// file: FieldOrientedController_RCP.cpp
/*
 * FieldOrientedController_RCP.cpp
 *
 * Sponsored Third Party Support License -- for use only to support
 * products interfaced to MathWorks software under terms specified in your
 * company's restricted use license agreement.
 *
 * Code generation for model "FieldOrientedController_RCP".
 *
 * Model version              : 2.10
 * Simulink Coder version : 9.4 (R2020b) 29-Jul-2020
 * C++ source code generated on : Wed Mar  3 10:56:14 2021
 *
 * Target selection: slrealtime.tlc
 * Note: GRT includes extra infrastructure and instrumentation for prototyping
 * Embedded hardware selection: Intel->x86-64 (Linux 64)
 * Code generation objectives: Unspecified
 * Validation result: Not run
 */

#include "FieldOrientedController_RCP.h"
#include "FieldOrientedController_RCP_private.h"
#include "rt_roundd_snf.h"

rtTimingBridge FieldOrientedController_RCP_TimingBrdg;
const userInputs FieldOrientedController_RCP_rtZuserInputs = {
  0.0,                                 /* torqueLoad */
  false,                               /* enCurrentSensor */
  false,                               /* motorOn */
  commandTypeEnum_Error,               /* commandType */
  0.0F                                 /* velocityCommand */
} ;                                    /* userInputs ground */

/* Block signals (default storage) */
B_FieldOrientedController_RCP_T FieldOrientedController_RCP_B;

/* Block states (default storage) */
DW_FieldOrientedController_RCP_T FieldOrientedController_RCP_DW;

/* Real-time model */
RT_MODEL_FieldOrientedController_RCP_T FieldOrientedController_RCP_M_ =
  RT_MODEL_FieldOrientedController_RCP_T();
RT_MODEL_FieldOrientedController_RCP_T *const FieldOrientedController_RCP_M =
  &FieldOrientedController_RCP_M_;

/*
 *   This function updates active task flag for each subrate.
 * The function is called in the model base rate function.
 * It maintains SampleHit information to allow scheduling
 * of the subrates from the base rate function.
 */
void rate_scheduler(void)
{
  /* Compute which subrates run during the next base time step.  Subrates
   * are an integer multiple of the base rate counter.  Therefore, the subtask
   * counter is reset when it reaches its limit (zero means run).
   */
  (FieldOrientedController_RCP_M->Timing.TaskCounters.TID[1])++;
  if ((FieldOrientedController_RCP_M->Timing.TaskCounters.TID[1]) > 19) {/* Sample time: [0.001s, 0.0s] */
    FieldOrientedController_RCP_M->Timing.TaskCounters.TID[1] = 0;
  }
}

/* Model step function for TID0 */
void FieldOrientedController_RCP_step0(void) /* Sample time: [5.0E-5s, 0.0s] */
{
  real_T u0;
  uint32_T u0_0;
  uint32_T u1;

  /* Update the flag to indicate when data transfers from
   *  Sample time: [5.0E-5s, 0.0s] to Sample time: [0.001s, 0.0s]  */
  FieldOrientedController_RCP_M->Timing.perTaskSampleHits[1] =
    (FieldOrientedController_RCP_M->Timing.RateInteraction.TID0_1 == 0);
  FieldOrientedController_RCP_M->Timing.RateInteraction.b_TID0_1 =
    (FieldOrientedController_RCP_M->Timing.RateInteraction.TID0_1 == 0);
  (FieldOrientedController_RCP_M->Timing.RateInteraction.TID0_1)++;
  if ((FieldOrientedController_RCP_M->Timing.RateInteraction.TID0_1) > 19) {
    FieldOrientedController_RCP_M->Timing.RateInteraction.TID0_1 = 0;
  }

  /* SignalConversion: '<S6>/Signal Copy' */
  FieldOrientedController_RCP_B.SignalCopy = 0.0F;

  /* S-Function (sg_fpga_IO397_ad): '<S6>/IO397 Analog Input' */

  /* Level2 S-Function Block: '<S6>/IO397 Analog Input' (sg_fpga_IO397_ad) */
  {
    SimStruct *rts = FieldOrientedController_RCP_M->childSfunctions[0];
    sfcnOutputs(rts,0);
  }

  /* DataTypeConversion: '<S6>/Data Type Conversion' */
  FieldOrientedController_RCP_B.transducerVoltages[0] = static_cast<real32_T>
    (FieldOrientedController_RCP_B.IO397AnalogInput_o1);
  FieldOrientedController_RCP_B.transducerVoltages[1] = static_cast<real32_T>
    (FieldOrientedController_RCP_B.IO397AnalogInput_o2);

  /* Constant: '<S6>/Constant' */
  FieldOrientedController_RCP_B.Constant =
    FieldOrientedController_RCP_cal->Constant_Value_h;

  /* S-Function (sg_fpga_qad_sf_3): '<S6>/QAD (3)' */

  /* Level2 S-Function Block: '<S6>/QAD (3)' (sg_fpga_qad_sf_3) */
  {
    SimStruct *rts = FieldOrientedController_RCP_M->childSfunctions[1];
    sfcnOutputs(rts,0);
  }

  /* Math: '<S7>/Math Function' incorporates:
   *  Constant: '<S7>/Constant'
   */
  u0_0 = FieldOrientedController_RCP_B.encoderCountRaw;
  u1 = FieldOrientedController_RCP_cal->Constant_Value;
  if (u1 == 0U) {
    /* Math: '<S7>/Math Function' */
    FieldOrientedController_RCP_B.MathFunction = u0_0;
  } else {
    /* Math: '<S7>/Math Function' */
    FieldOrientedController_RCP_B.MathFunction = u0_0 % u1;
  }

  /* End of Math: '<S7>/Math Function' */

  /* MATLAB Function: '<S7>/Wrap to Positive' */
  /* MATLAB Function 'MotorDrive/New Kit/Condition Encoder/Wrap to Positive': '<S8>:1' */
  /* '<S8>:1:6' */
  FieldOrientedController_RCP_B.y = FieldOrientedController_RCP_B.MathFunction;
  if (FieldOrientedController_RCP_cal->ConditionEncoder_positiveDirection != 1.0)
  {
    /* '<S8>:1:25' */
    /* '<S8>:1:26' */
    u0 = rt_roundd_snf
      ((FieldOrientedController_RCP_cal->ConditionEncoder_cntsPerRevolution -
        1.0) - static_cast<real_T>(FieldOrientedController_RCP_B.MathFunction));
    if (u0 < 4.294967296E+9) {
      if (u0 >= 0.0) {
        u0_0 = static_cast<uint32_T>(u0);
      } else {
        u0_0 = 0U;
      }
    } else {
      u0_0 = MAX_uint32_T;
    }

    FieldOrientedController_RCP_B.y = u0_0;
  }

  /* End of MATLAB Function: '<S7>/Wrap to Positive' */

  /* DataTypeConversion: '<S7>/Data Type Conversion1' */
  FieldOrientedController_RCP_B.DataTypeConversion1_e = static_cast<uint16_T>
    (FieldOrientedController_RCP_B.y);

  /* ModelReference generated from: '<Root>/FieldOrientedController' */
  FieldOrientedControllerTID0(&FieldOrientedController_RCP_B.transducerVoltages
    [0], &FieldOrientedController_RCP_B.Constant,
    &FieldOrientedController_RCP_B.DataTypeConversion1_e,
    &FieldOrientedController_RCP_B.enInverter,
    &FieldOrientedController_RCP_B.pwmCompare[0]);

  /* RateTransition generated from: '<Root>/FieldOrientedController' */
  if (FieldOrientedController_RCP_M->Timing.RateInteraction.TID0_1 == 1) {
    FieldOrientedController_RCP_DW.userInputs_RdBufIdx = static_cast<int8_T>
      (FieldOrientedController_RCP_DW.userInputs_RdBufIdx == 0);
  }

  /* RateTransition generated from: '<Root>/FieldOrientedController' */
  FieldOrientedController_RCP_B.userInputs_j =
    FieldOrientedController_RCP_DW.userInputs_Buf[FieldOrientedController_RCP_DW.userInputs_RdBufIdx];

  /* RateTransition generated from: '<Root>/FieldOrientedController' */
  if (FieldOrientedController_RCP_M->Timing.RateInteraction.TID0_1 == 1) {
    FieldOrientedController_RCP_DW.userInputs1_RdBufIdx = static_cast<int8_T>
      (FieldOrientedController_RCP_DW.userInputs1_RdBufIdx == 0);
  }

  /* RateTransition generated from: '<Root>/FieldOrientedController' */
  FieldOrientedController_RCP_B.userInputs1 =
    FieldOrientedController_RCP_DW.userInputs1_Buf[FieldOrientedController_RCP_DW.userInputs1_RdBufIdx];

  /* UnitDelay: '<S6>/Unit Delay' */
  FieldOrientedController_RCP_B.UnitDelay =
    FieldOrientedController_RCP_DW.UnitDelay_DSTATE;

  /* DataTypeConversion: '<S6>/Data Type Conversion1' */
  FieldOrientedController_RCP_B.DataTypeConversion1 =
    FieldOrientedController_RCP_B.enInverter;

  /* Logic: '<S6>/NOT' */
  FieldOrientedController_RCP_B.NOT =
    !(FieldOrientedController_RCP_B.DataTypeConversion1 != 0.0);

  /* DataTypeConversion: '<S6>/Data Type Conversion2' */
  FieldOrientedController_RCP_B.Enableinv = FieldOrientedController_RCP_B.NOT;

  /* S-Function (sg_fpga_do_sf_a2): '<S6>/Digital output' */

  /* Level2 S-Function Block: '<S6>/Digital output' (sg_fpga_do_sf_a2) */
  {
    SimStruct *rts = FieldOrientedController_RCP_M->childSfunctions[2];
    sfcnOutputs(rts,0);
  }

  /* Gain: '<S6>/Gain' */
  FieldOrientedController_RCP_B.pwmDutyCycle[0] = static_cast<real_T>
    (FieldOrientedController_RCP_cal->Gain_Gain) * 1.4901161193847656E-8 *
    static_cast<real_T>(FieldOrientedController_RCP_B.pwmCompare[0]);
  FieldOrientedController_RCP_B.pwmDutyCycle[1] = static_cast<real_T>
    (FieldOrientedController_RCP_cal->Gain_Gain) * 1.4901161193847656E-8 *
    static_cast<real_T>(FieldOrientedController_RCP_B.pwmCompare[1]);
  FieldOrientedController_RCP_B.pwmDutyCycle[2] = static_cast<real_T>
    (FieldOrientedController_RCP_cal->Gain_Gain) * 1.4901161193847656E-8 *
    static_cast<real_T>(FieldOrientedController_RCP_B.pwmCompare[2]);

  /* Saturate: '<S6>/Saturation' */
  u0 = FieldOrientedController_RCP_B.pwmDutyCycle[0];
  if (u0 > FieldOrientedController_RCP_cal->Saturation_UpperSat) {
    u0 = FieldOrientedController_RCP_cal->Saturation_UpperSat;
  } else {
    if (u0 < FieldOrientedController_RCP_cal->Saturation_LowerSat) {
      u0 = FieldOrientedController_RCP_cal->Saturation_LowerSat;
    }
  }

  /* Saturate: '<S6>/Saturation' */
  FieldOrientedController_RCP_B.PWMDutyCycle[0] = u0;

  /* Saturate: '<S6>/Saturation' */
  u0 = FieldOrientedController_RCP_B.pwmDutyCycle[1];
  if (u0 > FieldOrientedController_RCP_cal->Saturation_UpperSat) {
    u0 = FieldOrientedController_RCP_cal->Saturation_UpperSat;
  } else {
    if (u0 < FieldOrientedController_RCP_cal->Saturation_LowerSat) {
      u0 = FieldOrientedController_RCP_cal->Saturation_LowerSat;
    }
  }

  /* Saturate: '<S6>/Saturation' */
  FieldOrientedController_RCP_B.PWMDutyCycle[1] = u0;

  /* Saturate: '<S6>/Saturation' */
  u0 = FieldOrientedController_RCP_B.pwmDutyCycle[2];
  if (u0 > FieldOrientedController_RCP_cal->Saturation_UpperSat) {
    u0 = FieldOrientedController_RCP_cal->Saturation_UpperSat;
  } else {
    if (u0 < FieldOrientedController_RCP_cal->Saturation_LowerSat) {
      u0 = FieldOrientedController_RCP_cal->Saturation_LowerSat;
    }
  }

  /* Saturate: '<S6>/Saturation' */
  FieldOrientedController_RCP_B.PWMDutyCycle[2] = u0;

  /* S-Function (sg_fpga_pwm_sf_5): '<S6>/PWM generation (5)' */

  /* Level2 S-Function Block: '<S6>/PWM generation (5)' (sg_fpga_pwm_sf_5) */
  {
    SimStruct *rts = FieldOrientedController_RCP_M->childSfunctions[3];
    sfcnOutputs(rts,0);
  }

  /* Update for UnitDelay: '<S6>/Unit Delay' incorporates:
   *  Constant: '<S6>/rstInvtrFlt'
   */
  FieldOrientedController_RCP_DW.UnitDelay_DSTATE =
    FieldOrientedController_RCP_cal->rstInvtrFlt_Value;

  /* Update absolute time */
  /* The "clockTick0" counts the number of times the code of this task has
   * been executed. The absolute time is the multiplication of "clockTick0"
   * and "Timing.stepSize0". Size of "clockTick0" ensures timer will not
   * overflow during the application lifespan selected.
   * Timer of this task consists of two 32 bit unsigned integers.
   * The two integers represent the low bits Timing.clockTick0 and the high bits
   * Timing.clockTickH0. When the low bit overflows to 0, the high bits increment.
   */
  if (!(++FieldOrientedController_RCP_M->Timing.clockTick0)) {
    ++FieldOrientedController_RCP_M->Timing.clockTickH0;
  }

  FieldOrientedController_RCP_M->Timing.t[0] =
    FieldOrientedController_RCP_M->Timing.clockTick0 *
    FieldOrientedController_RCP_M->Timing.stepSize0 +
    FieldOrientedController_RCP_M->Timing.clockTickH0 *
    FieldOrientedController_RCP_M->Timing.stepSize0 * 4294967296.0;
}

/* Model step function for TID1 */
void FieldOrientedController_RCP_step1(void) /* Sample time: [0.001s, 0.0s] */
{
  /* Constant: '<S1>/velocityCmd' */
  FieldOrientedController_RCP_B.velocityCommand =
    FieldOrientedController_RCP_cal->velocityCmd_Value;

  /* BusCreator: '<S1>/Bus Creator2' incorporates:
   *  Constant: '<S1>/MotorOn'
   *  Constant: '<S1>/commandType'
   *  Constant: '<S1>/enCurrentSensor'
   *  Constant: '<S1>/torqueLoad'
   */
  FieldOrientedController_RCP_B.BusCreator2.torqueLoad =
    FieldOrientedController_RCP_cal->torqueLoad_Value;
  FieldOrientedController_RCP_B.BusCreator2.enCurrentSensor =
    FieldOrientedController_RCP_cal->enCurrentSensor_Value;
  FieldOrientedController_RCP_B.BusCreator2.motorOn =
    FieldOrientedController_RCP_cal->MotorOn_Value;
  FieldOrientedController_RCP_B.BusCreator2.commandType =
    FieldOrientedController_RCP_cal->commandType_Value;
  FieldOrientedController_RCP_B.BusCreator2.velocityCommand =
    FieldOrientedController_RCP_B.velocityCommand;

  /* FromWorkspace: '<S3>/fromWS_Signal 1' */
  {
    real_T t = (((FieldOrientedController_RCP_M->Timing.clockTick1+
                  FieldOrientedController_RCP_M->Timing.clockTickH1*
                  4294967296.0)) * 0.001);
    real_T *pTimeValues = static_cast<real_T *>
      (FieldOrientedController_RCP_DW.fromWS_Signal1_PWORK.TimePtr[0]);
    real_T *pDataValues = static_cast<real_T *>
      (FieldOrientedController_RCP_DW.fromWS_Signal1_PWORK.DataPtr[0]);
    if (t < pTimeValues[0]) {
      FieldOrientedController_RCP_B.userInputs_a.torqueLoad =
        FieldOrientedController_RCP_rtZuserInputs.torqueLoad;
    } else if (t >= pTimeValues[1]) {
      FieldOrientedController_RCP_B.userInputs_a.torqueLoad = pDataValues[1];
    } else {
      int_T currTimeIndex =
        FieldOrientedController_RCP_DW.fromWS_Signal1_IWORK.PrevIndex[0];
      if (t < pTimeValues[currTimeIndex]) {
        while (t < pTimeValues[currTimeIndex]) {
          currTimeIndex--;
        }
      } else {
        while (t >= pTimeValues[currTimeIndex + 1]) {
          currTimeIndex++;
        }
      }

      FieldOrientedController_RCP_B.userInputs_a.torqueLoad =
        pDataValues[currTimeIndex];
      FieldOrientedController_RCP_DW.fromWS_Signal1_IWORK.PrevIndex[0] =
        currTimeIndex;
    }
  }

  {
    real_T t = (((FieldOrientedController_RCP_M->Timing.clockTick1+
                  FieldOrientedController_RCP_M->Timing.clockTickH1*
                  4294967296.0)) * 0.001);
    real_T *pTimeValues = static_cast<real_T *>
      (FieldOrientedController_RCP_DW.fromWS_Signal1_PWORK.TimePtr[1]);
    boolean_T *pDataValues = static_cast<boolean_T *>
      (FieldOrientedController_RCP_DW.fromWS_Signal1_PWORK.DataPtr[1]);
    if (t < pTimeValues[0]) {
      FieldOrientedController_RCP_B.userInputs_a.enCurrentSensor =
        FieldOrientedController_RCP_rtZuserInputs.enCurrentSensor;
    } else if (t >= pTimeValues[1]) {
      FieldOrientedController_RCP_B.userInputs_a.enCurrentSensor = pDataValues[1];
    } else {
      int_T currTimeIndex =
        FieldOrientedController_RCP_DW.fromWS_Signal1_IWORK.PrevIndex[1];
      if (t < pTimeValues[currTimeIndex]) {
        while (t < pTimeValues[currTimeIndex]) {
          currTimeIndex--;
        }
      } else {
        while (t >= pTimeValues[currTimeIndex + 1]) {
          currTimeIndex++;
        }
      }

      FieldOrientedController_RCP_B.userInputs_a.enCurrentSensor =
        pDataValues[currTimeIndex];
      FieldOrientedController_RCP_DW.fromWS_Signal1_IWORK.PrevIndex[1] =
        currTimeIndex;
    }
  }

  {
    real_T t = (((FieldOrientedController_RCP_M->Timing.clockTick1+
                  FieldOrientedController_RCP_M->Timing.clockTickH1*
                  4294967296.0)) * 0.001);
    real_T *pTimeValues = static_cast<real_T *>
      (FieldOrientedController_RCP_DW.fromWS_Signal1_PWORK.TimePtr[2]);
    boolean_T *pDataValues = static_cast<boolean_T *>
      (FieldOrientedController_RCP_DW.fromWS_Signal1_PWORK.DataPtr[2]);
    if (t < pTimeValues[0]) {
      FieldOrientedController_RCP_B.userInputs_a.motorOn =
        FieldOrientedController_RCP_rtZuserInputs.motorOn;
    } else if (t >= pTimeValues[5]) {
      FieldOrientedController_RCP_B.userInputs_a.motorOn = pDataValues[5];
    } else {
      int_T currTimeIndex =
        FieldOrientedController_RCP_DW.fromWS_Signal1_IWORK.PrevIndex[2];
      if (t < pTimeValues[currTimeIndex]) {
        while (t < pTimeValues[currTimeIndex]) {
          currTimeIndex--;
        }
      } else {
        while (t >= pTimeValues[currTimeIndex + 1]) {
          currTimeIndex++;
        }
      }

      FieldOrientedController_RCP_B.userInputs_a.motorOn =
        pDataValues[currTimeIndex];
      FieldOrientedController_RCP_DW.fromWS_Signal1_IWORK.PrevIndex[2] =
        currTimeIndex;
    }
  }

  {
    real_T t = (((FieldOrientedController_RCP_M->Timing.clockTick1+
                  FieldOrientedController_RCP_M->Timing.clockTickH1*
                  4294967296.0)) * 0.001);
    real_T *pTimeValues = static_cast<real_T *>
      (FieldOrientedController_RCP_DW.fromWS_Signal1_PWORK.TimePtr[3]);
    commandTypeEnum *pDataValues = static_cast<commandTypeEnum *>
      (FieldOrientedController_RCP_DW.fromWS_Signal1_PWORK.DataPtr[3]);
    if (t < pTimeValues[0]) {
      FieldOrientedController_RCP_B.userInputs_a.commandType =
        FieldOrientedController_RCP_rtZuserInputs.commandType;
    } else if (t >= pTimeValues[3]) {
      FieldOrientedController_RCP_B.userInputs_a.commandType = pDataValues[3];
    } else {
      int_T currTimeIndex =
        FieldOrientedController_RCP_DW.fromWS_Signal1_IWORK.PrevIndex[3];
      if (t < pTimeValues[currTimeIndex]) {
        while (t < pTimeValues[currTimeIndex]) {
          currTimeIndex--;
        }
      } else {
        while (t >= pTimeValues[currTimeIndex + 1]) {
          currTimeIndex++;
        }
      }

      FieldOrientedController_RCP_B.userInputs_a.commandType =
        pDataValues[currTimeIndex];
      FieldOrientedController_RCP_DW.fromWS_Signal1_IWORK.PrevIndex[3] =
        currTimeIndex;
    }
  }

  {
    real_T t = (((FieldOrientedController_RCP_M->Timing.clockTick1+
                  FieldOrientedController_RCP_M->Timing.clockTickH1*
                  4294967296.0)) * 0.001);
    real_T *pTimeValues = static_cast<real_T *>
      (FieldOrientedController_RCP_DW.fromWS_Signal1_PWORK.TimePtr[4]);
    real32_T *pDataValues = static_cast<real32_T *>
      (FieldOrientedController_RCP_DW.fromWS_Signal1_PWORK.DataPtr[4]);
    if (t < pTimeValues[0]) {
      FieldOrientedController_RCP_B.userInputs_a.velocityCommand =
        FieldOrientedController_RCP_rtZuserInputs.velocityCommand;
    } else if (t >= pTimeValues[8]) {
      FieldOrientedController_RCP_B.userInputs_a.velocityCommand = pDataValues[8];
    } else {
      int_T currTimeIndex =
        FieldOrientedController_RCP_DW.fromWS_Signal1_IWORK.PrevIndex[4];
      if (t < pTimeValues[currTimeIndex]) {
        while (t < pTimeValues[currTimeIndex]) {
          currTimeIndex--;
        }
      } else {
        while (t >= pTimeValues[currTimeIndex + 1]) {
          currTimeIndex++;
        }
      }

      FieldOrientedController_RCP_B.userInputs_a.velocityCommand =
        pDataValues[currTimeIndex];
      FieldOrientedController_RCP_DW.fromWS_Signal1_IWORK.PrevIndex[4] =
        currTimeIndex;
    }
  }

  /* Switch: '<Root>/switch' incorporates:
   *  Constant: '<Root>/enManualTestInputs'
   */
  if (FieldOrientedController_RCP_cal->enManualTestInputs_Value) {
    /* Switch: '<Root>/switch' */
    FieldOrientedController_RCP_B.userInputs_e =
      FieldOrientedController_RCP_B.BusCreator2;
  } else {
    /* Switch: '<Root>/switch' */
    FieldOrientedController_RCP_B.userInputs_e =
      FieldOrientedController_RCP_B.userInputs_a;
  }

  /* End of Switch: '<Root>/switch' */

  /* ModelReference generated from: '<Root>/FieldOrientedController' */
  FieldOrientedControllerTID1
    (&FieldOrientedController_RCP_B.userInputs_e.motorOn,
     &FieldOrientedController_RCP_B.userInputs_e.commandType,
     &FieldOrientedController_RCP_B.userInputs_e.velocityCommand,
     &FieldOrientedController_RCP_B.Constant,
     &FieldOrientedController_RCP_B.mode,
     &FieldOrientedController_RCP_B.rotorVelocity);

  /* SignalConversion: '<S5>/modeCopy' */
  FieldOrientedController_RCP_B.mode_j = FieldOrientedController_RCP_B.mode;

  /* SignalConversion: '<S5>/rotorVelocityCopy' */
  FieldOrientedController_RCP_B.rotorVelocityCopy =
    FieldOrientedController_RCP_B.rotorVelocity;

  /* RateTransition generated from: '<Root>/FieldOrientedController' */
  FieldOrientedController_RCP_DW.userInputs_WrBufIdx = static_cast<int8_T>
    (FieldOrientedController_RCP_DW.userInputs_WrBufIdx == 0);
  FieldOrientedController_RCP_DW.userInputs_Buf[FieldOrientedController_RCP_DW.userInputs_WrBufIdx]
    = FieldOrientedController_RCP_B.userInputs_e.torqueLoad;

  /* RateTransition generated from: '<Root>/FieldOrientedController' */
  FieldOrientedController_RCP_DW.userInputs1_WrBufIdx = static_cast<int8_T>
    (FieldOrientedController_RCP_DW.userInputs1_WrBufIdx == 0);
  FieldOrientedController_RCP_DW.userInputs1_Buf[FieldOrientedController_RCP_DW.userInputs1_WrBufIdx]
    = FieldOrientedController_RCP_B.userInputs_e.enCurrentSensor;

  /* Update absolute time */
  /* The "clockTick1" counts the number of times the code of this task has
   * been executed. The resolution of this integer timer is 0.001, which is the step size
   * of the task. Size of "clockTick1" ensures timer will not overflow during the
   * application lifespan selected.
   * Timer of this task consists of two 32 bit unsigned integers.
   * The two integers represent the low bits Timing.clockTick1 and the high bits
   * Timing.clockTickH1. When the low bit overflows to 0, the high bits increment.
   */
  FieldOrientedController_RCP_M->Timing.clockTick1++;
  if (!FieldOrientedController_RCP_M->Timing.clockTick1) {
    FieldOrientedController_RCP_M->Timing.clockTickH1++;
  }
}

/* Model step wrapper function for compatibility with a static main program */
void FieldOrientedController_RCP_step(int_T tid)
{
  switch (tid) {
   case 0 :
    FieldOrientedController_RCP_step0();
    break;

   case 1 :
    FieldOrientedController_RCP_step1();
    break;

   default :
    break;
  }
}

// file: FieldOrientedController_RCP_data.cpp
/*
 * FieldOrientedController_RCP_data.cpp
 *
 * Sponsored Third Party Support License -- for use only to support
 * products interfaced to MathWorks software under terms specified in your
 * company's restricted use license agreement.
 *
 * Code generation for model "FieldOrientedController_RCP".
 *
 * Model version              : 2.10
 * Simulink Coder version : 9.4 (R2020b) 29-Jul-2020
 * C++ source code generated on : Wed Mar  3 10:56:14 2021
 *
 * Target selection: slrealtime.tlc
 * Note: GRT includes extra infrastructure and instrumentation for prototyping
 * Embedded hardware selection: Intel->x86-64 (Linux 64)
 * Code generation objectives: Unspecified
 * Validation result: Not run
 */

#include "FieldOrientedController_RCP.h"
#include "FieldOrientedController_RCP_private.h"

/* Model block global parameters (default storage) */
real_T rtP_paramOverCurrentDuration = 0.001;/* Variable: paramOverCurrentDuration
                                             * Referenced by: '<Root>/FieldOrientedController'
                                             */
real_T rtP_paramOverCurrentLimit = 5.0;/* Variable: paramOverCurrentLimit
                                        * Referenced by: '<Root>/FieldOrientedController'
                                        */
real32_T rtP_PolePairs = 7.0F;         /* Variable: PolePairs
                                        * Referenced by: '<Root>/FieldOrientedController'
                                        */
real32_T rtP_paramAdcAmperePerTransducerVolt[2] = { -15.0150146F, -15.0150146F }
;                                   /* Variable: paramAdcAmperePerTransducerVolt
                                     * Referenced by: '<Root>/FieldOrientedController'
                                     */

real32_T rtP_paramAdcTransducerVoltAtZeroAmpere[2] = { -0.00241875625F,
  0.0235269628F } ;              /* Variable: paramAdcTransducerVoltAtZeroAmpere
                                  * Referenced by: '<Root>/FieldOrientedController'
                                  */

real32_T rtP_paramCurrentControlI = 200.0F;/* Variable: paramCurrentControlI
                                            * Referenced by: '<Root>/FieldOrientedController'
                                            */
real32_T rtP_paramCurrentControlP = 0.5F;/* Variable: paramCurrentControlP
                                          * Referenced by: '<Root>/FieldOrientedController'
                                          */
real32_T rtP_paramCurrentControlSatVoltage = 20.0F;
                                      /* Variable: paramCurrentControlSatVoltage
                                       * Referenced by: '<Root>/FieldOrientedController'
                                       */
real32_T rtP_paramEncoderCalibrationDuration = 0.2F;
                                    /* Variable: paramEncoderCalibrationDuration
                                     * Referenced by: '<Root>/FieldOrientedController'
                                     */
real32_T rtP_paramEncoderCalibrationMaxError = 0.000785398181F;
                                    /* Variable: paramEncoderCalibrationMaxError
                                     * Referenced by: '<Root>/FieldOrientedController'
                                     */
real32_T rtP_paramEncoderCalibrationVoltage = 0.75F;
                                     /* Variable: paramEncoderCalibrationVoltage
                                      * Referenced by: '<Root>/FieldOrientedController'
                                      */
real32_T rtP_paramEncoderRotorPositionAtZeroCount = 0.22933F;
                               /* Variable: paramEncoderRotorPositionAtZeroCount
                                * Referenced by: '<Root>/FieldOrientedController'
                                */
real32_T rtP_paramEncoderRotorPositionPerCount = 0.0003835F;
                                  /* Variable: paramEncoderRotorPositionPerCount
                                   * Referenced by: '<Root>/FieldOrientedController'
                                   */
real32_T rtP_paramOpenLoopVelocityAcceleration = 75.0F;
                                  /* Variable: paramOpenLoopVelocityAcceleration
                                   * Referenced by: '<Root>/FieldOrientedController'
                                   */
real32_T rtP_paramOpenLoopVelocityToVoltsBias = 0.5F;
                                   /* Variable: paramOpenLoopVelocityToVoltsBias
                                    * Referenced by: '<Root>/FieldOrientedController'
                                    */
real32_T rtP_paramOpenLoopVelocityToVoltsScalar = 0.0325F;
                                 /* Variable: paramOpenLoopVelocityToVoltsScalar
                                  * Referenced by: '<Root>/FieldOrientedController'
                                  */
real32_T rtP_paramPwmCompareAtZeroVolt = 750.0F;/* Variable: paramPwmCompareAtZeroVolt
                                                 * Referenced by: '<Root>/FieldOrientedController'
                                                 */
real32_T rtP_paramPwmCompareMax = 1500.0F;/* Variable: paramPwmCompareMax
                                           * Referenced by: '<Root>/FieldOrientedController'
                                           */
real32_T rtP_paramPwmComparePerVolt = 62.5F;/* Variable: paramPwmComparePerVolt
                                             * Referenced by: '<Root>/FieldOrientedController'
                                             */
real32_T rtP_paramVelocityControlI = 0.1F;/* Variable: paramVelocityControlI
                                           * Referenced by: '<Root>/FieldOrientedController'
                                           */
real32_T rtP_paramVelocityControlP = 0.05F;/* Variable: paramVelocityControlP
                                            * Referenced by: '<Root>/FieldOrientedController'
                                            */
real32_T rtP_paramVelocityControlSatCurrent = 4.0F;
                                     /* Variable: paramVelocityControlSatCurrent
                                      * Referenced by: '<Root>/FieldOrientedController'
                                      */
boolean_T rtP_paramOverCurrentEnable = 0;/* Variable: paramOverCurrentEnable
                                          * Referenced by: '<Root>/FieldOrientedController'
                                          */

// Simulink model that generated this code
simulink model "FieldOrientedController_RCP"  (R2020b)
settings: configuration reference "SLRT" (kept outside this file)
undefined symbols (not defined in the file): commandTypeEnum, encoder, IO397, pwm, sampleTime
libraries: speedgoatlib_fpga_dio x2, speedgoatlib_fpga_analog_io x2, speedgoatlib_fpga_pwm x2, speedgoatlib_fpga_quadrature x2, speedgoatlib_fpga x2, SignalEditorBlockLib x1

== system FieldOrientedController_RCP ==
  Callback Button : CallbackButton  ButtonText=Switch Electric Motor Control Kit
  FieldOrientedController : ModelReference  ModelNameDialog=FieldOrientedController  SimulationMode=Normal  ModelReferenceVersion=1.564
  ManualTestInputs : Subsystem  Description=""  VariantControl=TestInputChoice == 2
  MotorDrive : Subsystem  Variant=on  VariantControl=demoMode == 2
  SignalEditor_Experiments : SignalEditorBlockLib/Signal Editor  FileName=PMSM_Experiments.mat  ActiveScenario=ClosedLoop_CoastdownTest  ActiveSignal=userInputs  IsBus=on  OutputBusObjectStr=Bus: userInputs  SampleTime=sampleTime.VelocityControl  Interpolate=off  ZeroCross=off  OutputAfterFinalValue=Holding final value  Unit=inherit  PreserveSignalName=on
  UserInterface : Subsystem
  enManualTestInputs : Constant  Value=0  OutDataTypeStr=boolean
  log : Subsystem
  switch : Switch  Criteria=u2 ~= 0
  wires:
  FieldOrientedController/2 -> MotorDrive/1("motorCommands  ")  "motorCommands"
  MotorDrive/1(" controllerFeedback") -> FieldOrientedController/2  "controllerFeedback"
  SignalEditor_Experiments/1 -> switch/3  "userInputs"
  ManualTestInputs/1(userInputs) -> switch/1  "userInputs"
  switch/1 -> FieldOrientedController/1  "userInputs"
  enManualTestInputs/1 -> switch/2
  FieldOrientedController/1 -> log/1(In)  "controllerInfo"

== system FieldOrientedController_RCP/ManualTestInputs ==
  note: (rad/sec)
  Bus Creator2 : BusCreator  Inputs=5  OutDataTypeStr=Bus: userInputs  NonVirtualBus=on
  MotorOn : Constant  Value=logical(1)  OutDataTypeStr=boolean  SampleTime=sampleTime.VelocityControl
  commandType : Constant  Value=commandTypeEnum(3)  SampleTime=sampleTime.VelocityControl
  enCurrentSensor : Constant  Value=logical(1)  OutDataTypeStr=boolean  SampleTime=sampleTime.VelocityControl
  torqueLoad : Constant  Value=0  OutDataTypeStr=double  SampleTime=sampleTime.VelocityControl
  velocityCmd : Constant  Value=50  OutDataTypeStr=single  SampleTime=sampleTime.VelocityControl
  userInputs : Outport  VectorParamsAs1DForOutWhenUnconnected=off
  wires:
  MotorOn/1 -> Bus Creator2/3  "motorOn"
  commandType/1 -> Bus Creator2/4  "commandType"
  torqueLoad/1 -> Bus Creator2/1  "torqueLoad"
  enCurrentSensor/1 -> Bus Creator2/2  "enCurrentSensor"
  Bus Creator2/1 -> userInputs/1
  velocityCmd/1 -> Bus Creator2/5  "velocityCommand"

== system FieldOrientedController_RCP/MotorDrive ==
  "motorCommands  " : Inport
  New Kit : Subsystem  VariantControl=kitType == 1
  Old Kit : Subsystem  VariantControl=kitType == 2
  " controllerFeedback" : Outport  OutDataTypeStr=Bus: controllerFeedback  VectorParamsAs1DForOutWhenUnconnected=off

== system FieldOrientedController_RCP/UserInterface ==
  note: Inputs
  note: Outputs
  Dashboard Scope : DashboardScope  TimeSpan=10  Ymin=-250  Ymax=250  ScaleAtStop=off
  Display : DisplayBlock  LabelPosition=Hide  Format=short  Transparency=1
  Knob : KnobBlock  ScaleMin=-250  ScaleMax=250  TickInterval=50
  Lamp : LampBlock
  Rotary Switch : RotarySwitchBlock  UseEnumeratedDataType=on  EnumeratedDataType=commandTypeEnum
  Toggle Switch1 : ToggleSwitchBlock
  Toggle Switch2 : ToggleSwitchBlock

== system FieldOrientedController_RCP/log ==
  mode : Inport  PortName=In  Element=mode
  rotorVelocity : Inport  PortName=In  Element=rotorVelocity
  Terminator : Terminator
  Terminator1 : Terminator
  modeCopy : SignalConversion  OverrideOpt=on
  rotorVelocityCopy : SignalConversion  OverrideOpt=on
  wires:
  rotorVelocity/1 -> rotorVelocityCopy/1
  mode/1 -> modeCopy/1
  rotorVelocityCopy/1 -> Terminator/1  "rotorVelocity"
  modeCopy/1 -> Terminator1/1  "mode"

== system FieldOrientedController_RCP/MotorDrive/New Kit ==
  note: Speedgoat Outputs
  note: Speedgoat Inputs
  Bus Element In : Inport  PortName=motorCommands  Element=enInverter
  Bus Element In1 : Inport  PortName=motorCommands  Element=pwmCompare
  Condition Encoder : Subsystem  mask(Speedgoat Encoder Counter){cntsPerRevolution=encoder.CountPerRevolution, positiveDirection=encoder.ALeadsB}
      mask prompts: cntsPerRevolution "Counts per revolution"; positiveDirection "A leads B?"
      mask help: Configures the direction and positive range of the counter value returned by the Speedgoat IO313 QAD Read block.
      mask init:
      | if positiveDirection == 1
      |     strPositiveDirection = 'A Leads B';
      | else
      |     strPositiveDirection = 'B Leads A';
      | end
  Constant : Constant  Value=true  SampleTime=sampleTime.CurrentControl
  Data Type Conversion : DataTypeConversion  OutDataTypeStr=single
  Data Type Conversion1 : DataTypeConversion  OutDataTypeStr=double
  Data Type Conversion2 : DataTypeConversion
  Digital output : speedgoatlib_fpga_dio/Digital output  id=1  chan=[1 4 5]  init=[1 0 0]  reset=[1 1 1]  vectorizeInput=off  ts=-1  pciSlot=-1  board=IO397-50k
  Gain : Gain  Gain=1/pwm.CounterMax  OutDataTypeStr=double
  Ground : Ground
  IO397 Analog Input : speedgoatlib_fpga_analog_io/IO397 Analog Input  id=1  chan=[1:2]  range=+-5.12 V  trigger=Target  ts=sampleTime.CurrentControl  pciSlot=-1  board=IO397-50k
  Mux : Mux  Inputs=2
  NOT : Logic  Operator=NOT  IconShape=distinctive  AllPortsSameDT=off  OutDataTypeStr=boolean
  PWM generation (5) : speedgoatlib_fpga_pwm/PWM generation (5)  id=1  chan=[1 2 3]  board=IO397-50k  ts=-1  pciSlot=-1  delay=0  symmetric=Symmetric - PWM generation is centered around half the period  b_is_complement_of_a=The complement of PWM A output  deadband=[0.0]  period=pwm.Period  frequency=25000  ticks=2999  a_on=[0]  a_off=[0]  pwm_a_dc=[0.5]  b_on=[0]  b_off=[0]  pwm_b_dc=[0]  c_on=[0.0]  c_off=[0.0]  protection=B is forced off when A is on.  enable_latch_half_period=off  pwm_update=At period starts  trigger_duration=[1e-6]  trigger_period_start=on  trigger_half_of_the_period=off  trigger_a_on=off  trigger_a_off=off  trigger_b_on=off  trigger_b_off=off  show_a_input=on  show_b_input=on  show_c_input=off  show_period_input=off  show_force_stop_input=off  idle_a=Low when PWM generation is halted  idle_b=Low when PWM generation is halted  idle_c=Low when PWM generation is halted  cancels_pwm_generation=on  invert_a=off  invert_b=off  invert_c=off
  QAD (3) : speedgoatlib_fpga_quadrature/QAD (3)  id=1  board=IO397-50k  chan=[1]  resetOnStart=on  ts=sampleTime.CurrentControl  pciSlot=-1  operatingMode=Quadrature decoder  indexControlMode=Ignore index  resolution=4x  stepsPerRevolution=encoder.CountPerRevolution  latchMode=Disabled  interpolatePosition=off  invertAB=off  showClearPositionInput=off  showClearIndexFoundInput=off  showPositionOutput=on  showTurnOutput=off  showSpeedOutput=off  showDirectionOutput=off  showIndexFoundOutput=off
  Saturation : Saturate  UpperLimit=1  LowerLimit=0
  Setup1 : speedgoatlib_fpga/Setup/Setup  board=IO397-50k  id=1  device_id=1  frontIO=None  rearIO=None  bitstreamFile=speedgoat_IO397_50k_CI_02009  rev=1.0  timestamp_string=27/11/19 11:18:03  fpgaFreq=75 MHz  fpgaTick=13.3333 ns  ProgSpiFlash=off  ProgBPIFlash=off  pciSlot=-1  PullRPort0=pull-up 3.3V  VioPort0=3.3V  PullRPort1=pull-up 3.3V  VioPort1=3.3V  PullRPort2=pull-up 3.3V  VioPort2=3.3V  PullRPort3=pull-up 3.3V  VioPort3=3.3V  PullRPort4=pull-up 3.3V  VioPort4=3.3V  PullRPort5=pull-up 3.3V  VioPort5=3.3V  PullRPort6=pull-up 3.3V  VioPort6=3.3V  PullRPort15=pull-up 3.3V  PullRPort31=pull-up 3.3V  PullRPort47=pull-up 3.3V  PullRPort63=pull-up 3.3V
  Signal Copy : SignalConversion  OverrideOpt=off
  Unit Delay : UnitDelay  InitialCondition=1  SampleTime=-1  HasFrameUpgradeWarning=on
  rstInvtrFlt : Constant  Value=0
  Out Bus Element4 : Outport  VectorParamsAs1DForOutWhenUnconnected=off  PortName=controllerFeedback  Element=rotorVelocity
  Out Bus Element1 : Outport  VectorParamsAs1DForOutWhenUnconnected=off  PortName=controllerFeedback  Element=transducerVoltage
  Out Bus Element3 : Outport  VectorParamsAs1DForOutWhenUnconnected=off  PortName=controllerFeedback  Element=encoderIndexFound
  Out Bus Element2 : Outport  VectorParamsAs1DForOutWhenUnconnected=off  PortName=controllerFeedback  Element=encoderCount
  wires:
  Constant/1 -> Out Bus Element3/1
  Gain/1 -> Saturation/1  "pwmDutyCycle"
  Saturation/1 -> PWM generation (5)/1  "PWM Duty Cycle"
  Bus Element In1/1 -> Gain/1
  Condition Encoder/1(Out1) -> Out Bus Element2/1  "encoderCount"
  IO397 Analog Input/2 -> Mux/2
  IO397 Analog Input/1 -> Mux/1
  Data Type Conversion2/1 -> Digital output/3  "Enable inv"
  NOT/1 -> Data Type Conversion2/1
  QAD (3)/1 -> Condition Encoder/1(In1)  "encoderCountRaw"
  Bus Element In/1 -> Data Type Conversion1/1
  Mux/1 -> Data Type Conversion/1  "transducerVoltages"
  rstInvtrFlt/1 -> Unit Delay/1  "Fault Reset"
  Unit Delay/1 -> Digital output/1
  Data Type Conversion/1 -> Out Bus Element1/1  "transducerVoltages"
  Data Type Conversion1/1 -> NOT/1, Digital output/2
  Ground/1 -> Signal Copy/1
  Signal Copy/1 -> Out Bus Element4/1

== system FieldOrientedController_RCP/MotorDrive/Old Kit ==
  note: Speedgoat Inputs
  note: Speedgoat Outputs
  Bus Element In : Inport  PortName=motorCommands  Element=enInverter
  Bus Element In1 : Inport  PortName=motorCommands  Element=pwmCompare
  Condition Encoder : Subsystem  mask(Speedgoat Encoder Counter){cntsPerRevolution=encoder.CountPerRevolution, positiveDirection=encoder.ALeadsB}
      mask prompts: cntsPerRevolution "Counts per revolution"; positiveDirection "A leads B?"
      mask help: Configures the direction and positive range of the counter value returned by the Speedgoat IO313 QAD Read block.
      mask init:
      | if positiveDirection == 1
      |     strPositiveDirection = 'A Leads B';
      | else
      |     strPositiveDirection = 'B Leads A';
      | end
  Data Type Conversion : DataTypeConversion  OutDataTypeStr=boolean
  Data Type Conversion1 : DataTypeConversion  OutDataTypeStr=int32
  Digital output : speedgoatlib_fpga_dio/Digital output  id=1  chan=[2:4]  init=0  reset=0  vectorizeInput=off  ts=-1  pciSlot=-1  board=IO397-50k
  Gain : Gain  Gain=1/pwm.CounterMax
  Ground : Ground
  IO397 Analog Input : speedgoatlib_fpga_analog_io/IO397 Analog Input  id=1  chan=[1:2]  range=+5.12 V  trigger=Target  ts=sampleTime.CurrentControl  pciSlot=-1  board=IO397-50k
  Mux : Mux  Inputs=2
  PWM generation (5) : speedgoatlib_fpga_pwm/PWM generation (5)  id=1  chan=[1 2 3]  board=IO397-50k  ts=-1  pciSlot=-1  delay=0  symmetric=Symmetric - PWM generation is centered around half the period  b_is_complement_of_a=The complement of PWM A output  deadband=[0.0]  period=pwm.Period  frequency=25000  ticks=2999  a_on=[0]  a_off=[0]  pwm_a_dc=[0.5]  b_on=[0]  b_off=[0]  pwm_b_dc=[0]  c_on=[0.0]  c_off=[0.0]  protection=B is forced off when A is on.  enable_latch_half_period=off  pwm_update=At period starts  trigger_duration=[1e-6]  trigger_period_start=on  trigger_half_of_the_period=off  trigger_a_on=off  trigger_a_off=off  trigger_b_on=off  trigger_b_off=off  show_a_input=on  show_b_input=on  show_c_input=off  show_period_input=off  show_force_stop_input=off  idle_a=Low when PWM generation is halted  idle_b=Low when PWM generation is halted  idle_c=Low when PWM generation is halted  cancels_pwm_generation=on  invert_a=off  invert_b=off  invert_c=off
  QAD (3) : speedgoatlib_fpga_quadrature/QAD (3)  id=1  board=IO397-50k  chan=[1]  resetOnStart=on  ts=sampleTime.CurrentControl  pciSlot=-1  operatingMode=Quadrature decoder  indexControlMode=Ignore index  resolution=4x  stepsPerRevolution=encoder.CountPerRevolution  latchMode=Disabled  interpolatePosition=off  invertAB=off  showClearPositionInput=off  showClearIndexFoundInput=off  showPositionOutput=on  showTurnOutput=off  showSpeedOutput=off  showDirectionOutput=off  showIndexFoundOutput=on
  Saturation : Saturate  UpperLimit=1  LowerLimit=0
  Setup1 : speedgoatlib_fpga/Setup/Setup  board=IO397-50k  id=1  device_id=1  frontIO=None  rearIO=None  bitstreamFile=speedgoat_IO397_50k_CI_IO397_PMSM_DEMO  rev=1.0  timestamp_string=23/06/34 18:45:29  fpgaFreq=75 MHz  fpgaTick=13.3333 ns  ProgSpiFlash=off  ProgBPIFlash=off  pciSlot=-1  PullRPort0=pull-up 3.3V  VioPort0=3.3V  PullRPort1=pull-up 3.3V  VioPort1=3.3V  PullRPort2=pull-up 3.3V  VioPort2=3.3V  PullRPort3=pull-up 3.3V  VioPort3=3.3V  PullRPort4=pull-up 3.3V  VioPort4=3.3V  PullRPort5=pull-up 3.3V  VioPort5=3.3V  PullRPort6=pull-up 3.3V  VioPort6=3.3V  PullRPort15=pull-up 3.3V  PullRPort31=pull-up 3.3V  PullRPort47=pull-up 3.3V  PullRPort63=pull-up 3.3V
  Signal Copy : SignalConversion  OverrideOpt=off
  Out Bus Element1 : Outport  VectorParamsAs1DForOutWhenUnconnected=off  PortName=controllerFeedback  Element=rotorVelocity
  Out Bus Element2 : Outport  VectorParamsAs1DForOutWhenUnconnected=off  PortName=controllerFeedback  Element=encoderCount
  Out Bus Element3 : Outport  VectorParamsAs1DForOutWhenUnconnected=off  PortName=controllerFeedback  Element=encoderIndexFound
  Out Bus Element4 : Outport  PortName=controllerFeedback  Element=transducerVoltage
  wires:
  Saturation/1 -> PWM generation (5)/1  "PWM Duty Cycle"
  Bus Element In1/1 -> Gain/1
  Gain/1 -> Saturation/1  "pwmDutyCycle"
  Bus Element In/1 -> Digital output/1, Digital output/3, Digital output/2
  Condition Encoder/1(Out1) -> Out Bus Element2/1
  Mux/1 -> Out Bus Element4/1
  IO397 Analog Input/2 -> Mux/2
  Data Type Conversion1/1 -> Condition Encoder/1(In1)
  QAD (3)/1 -> Data Type Conversion1/1  "encoderCountRaw"
  Data Type Conversion/1 -> Out Bus Element3/1
  QAD (3)/2 -> Data Type Conversion/1  "encoderIndexFoundRaw"
  IO397 Analog Input/1 -> Mux/1
  Ground/1 -> Signal Copy/1
  Signal Copy/1 -> Out Bus Element1/1

== system FieldOrientedController_RCP/MotorDrive/New Kit/Condition Encoder ==
  In1 : Inport
  Constant : Constant  Value=encoder.CountPerRevolution  OutDataTypeStr=uint32
  Data Type Conversion1 : DataTypeConversion  OutDataTypeStr=uint16
  Math Function : Math  Operator=mod  SignedPower=on  SaturateOnIntegerOverflow=on
  Wrap to Positive : MATLAB Function  TreatAsAtomicUnit=on
  Out1 : Outport  VectorParamsAs1DForOutWhenUnconnected=off
  wires:
  Math Function/1 -> Wrap to Positive/1(u)
  Constant/1 -> Math Function/2
  Wrap to Positive/1(y) -> Data Type Conversion1/1
  In1/1 -> Math Function/1
  Data Type Conversion1/1 -> Out1/1

== system FieldOrientedController_RCP/MotorDrive/Old Kit/Condition Encoder ==
  In1 : Inport
  Constant : Constant  Value=encoder.CountPerRevolution  OutDataTypeStr=int32
  Data Type Conversion : DataTypeConversion  OutDataTypeStr=int32
  Data Type Conversion1 : DataTypeConversion  OutDataTypeStr=uint16
  Math Function : Math  Operator=mod  SignedPower=on  SaturateOnIntegerOverflow=on
  Wrap to Positive : MATLAB Function  TreatAsAtomicUnit=on
  Out1 : Outport  VectorParamsAs1DForOutWhenUnconnected=off
  wires:
  Math Function/1 -> Wrap to Positive/1(u)
  Constant/1 -> Math Function/2
  In1/1 -> Data Type Conversion/1
  Wrap to Positive/1(y) -> Data Type Conversion1/1
  Data Type Conversion/1 -> Math Function/1
  Data Type Conversion1/1 -> Out1/1

== matlab function FieldOrientedController_RCP/MotorDrive/Old Kit/Condition Encoder/Wrap to Positive ==
function y = fcn(u,cntsPerRevolution,positiveDirection)
% Guarantee the count is between 0 and cntsPerRevolution
% (Speedgoat count can be negative)

% Simplest case
y=u;

% % Max consecutive index pulses that can be missed
% maxIndexPulseMissesToRecoverFrom = 2;
% 
% for index = 1:maxIndexPulseMissesToRecoverFrom
%     if y >= cntsPerRevolution
%         y = y - cntsPerRevolution;
%     elseif y < -cntsPerRevolution
%         y = y + cntsPerRevolution;
%     end
% end
% 
% % Wrap angle to positive value
% if (y<0)
%     y = cntsPerRevolution + y;
% end

% Handle case of swapping encoder A & B signals
if positiveDirection ~= 1
    y = (cntsPerRevolution-1) - y;
end

== matlab function FieldOrientedController_RCP/MotorDrive/New Kit/Condition Encoder/Wrap to Positive ==
function y = fcn(u,cntsPerRevolution,positiveDirection)
% Guarantee the count is between 0 and cntsPerRevolution
% (Speedgoat count can be negative)

% Simplest case
y=u;

% % Max consecutive index pulses that can be missed
% maxIndexPulseMissesToRecoverFrom = 2;
% 
% for index = 1:maxIndexPulseMissesToRecoverFrom
%     if y >= cntsPerRevolution
%         y = y - cntsPerRevolution;
%     elseif y < -cntsPerRevolution
%         y = y + cntsPerRevolution;
%     end
% end
% 
% % Wrap angle to positive value
% if (y<0)
%     y = cntsPerRevolution + y;
% end

% Handle case of swapping encoder A & B signals
if positiveDirection ~= 1
    y = (cntsPerRevolution-1) - y;
end
